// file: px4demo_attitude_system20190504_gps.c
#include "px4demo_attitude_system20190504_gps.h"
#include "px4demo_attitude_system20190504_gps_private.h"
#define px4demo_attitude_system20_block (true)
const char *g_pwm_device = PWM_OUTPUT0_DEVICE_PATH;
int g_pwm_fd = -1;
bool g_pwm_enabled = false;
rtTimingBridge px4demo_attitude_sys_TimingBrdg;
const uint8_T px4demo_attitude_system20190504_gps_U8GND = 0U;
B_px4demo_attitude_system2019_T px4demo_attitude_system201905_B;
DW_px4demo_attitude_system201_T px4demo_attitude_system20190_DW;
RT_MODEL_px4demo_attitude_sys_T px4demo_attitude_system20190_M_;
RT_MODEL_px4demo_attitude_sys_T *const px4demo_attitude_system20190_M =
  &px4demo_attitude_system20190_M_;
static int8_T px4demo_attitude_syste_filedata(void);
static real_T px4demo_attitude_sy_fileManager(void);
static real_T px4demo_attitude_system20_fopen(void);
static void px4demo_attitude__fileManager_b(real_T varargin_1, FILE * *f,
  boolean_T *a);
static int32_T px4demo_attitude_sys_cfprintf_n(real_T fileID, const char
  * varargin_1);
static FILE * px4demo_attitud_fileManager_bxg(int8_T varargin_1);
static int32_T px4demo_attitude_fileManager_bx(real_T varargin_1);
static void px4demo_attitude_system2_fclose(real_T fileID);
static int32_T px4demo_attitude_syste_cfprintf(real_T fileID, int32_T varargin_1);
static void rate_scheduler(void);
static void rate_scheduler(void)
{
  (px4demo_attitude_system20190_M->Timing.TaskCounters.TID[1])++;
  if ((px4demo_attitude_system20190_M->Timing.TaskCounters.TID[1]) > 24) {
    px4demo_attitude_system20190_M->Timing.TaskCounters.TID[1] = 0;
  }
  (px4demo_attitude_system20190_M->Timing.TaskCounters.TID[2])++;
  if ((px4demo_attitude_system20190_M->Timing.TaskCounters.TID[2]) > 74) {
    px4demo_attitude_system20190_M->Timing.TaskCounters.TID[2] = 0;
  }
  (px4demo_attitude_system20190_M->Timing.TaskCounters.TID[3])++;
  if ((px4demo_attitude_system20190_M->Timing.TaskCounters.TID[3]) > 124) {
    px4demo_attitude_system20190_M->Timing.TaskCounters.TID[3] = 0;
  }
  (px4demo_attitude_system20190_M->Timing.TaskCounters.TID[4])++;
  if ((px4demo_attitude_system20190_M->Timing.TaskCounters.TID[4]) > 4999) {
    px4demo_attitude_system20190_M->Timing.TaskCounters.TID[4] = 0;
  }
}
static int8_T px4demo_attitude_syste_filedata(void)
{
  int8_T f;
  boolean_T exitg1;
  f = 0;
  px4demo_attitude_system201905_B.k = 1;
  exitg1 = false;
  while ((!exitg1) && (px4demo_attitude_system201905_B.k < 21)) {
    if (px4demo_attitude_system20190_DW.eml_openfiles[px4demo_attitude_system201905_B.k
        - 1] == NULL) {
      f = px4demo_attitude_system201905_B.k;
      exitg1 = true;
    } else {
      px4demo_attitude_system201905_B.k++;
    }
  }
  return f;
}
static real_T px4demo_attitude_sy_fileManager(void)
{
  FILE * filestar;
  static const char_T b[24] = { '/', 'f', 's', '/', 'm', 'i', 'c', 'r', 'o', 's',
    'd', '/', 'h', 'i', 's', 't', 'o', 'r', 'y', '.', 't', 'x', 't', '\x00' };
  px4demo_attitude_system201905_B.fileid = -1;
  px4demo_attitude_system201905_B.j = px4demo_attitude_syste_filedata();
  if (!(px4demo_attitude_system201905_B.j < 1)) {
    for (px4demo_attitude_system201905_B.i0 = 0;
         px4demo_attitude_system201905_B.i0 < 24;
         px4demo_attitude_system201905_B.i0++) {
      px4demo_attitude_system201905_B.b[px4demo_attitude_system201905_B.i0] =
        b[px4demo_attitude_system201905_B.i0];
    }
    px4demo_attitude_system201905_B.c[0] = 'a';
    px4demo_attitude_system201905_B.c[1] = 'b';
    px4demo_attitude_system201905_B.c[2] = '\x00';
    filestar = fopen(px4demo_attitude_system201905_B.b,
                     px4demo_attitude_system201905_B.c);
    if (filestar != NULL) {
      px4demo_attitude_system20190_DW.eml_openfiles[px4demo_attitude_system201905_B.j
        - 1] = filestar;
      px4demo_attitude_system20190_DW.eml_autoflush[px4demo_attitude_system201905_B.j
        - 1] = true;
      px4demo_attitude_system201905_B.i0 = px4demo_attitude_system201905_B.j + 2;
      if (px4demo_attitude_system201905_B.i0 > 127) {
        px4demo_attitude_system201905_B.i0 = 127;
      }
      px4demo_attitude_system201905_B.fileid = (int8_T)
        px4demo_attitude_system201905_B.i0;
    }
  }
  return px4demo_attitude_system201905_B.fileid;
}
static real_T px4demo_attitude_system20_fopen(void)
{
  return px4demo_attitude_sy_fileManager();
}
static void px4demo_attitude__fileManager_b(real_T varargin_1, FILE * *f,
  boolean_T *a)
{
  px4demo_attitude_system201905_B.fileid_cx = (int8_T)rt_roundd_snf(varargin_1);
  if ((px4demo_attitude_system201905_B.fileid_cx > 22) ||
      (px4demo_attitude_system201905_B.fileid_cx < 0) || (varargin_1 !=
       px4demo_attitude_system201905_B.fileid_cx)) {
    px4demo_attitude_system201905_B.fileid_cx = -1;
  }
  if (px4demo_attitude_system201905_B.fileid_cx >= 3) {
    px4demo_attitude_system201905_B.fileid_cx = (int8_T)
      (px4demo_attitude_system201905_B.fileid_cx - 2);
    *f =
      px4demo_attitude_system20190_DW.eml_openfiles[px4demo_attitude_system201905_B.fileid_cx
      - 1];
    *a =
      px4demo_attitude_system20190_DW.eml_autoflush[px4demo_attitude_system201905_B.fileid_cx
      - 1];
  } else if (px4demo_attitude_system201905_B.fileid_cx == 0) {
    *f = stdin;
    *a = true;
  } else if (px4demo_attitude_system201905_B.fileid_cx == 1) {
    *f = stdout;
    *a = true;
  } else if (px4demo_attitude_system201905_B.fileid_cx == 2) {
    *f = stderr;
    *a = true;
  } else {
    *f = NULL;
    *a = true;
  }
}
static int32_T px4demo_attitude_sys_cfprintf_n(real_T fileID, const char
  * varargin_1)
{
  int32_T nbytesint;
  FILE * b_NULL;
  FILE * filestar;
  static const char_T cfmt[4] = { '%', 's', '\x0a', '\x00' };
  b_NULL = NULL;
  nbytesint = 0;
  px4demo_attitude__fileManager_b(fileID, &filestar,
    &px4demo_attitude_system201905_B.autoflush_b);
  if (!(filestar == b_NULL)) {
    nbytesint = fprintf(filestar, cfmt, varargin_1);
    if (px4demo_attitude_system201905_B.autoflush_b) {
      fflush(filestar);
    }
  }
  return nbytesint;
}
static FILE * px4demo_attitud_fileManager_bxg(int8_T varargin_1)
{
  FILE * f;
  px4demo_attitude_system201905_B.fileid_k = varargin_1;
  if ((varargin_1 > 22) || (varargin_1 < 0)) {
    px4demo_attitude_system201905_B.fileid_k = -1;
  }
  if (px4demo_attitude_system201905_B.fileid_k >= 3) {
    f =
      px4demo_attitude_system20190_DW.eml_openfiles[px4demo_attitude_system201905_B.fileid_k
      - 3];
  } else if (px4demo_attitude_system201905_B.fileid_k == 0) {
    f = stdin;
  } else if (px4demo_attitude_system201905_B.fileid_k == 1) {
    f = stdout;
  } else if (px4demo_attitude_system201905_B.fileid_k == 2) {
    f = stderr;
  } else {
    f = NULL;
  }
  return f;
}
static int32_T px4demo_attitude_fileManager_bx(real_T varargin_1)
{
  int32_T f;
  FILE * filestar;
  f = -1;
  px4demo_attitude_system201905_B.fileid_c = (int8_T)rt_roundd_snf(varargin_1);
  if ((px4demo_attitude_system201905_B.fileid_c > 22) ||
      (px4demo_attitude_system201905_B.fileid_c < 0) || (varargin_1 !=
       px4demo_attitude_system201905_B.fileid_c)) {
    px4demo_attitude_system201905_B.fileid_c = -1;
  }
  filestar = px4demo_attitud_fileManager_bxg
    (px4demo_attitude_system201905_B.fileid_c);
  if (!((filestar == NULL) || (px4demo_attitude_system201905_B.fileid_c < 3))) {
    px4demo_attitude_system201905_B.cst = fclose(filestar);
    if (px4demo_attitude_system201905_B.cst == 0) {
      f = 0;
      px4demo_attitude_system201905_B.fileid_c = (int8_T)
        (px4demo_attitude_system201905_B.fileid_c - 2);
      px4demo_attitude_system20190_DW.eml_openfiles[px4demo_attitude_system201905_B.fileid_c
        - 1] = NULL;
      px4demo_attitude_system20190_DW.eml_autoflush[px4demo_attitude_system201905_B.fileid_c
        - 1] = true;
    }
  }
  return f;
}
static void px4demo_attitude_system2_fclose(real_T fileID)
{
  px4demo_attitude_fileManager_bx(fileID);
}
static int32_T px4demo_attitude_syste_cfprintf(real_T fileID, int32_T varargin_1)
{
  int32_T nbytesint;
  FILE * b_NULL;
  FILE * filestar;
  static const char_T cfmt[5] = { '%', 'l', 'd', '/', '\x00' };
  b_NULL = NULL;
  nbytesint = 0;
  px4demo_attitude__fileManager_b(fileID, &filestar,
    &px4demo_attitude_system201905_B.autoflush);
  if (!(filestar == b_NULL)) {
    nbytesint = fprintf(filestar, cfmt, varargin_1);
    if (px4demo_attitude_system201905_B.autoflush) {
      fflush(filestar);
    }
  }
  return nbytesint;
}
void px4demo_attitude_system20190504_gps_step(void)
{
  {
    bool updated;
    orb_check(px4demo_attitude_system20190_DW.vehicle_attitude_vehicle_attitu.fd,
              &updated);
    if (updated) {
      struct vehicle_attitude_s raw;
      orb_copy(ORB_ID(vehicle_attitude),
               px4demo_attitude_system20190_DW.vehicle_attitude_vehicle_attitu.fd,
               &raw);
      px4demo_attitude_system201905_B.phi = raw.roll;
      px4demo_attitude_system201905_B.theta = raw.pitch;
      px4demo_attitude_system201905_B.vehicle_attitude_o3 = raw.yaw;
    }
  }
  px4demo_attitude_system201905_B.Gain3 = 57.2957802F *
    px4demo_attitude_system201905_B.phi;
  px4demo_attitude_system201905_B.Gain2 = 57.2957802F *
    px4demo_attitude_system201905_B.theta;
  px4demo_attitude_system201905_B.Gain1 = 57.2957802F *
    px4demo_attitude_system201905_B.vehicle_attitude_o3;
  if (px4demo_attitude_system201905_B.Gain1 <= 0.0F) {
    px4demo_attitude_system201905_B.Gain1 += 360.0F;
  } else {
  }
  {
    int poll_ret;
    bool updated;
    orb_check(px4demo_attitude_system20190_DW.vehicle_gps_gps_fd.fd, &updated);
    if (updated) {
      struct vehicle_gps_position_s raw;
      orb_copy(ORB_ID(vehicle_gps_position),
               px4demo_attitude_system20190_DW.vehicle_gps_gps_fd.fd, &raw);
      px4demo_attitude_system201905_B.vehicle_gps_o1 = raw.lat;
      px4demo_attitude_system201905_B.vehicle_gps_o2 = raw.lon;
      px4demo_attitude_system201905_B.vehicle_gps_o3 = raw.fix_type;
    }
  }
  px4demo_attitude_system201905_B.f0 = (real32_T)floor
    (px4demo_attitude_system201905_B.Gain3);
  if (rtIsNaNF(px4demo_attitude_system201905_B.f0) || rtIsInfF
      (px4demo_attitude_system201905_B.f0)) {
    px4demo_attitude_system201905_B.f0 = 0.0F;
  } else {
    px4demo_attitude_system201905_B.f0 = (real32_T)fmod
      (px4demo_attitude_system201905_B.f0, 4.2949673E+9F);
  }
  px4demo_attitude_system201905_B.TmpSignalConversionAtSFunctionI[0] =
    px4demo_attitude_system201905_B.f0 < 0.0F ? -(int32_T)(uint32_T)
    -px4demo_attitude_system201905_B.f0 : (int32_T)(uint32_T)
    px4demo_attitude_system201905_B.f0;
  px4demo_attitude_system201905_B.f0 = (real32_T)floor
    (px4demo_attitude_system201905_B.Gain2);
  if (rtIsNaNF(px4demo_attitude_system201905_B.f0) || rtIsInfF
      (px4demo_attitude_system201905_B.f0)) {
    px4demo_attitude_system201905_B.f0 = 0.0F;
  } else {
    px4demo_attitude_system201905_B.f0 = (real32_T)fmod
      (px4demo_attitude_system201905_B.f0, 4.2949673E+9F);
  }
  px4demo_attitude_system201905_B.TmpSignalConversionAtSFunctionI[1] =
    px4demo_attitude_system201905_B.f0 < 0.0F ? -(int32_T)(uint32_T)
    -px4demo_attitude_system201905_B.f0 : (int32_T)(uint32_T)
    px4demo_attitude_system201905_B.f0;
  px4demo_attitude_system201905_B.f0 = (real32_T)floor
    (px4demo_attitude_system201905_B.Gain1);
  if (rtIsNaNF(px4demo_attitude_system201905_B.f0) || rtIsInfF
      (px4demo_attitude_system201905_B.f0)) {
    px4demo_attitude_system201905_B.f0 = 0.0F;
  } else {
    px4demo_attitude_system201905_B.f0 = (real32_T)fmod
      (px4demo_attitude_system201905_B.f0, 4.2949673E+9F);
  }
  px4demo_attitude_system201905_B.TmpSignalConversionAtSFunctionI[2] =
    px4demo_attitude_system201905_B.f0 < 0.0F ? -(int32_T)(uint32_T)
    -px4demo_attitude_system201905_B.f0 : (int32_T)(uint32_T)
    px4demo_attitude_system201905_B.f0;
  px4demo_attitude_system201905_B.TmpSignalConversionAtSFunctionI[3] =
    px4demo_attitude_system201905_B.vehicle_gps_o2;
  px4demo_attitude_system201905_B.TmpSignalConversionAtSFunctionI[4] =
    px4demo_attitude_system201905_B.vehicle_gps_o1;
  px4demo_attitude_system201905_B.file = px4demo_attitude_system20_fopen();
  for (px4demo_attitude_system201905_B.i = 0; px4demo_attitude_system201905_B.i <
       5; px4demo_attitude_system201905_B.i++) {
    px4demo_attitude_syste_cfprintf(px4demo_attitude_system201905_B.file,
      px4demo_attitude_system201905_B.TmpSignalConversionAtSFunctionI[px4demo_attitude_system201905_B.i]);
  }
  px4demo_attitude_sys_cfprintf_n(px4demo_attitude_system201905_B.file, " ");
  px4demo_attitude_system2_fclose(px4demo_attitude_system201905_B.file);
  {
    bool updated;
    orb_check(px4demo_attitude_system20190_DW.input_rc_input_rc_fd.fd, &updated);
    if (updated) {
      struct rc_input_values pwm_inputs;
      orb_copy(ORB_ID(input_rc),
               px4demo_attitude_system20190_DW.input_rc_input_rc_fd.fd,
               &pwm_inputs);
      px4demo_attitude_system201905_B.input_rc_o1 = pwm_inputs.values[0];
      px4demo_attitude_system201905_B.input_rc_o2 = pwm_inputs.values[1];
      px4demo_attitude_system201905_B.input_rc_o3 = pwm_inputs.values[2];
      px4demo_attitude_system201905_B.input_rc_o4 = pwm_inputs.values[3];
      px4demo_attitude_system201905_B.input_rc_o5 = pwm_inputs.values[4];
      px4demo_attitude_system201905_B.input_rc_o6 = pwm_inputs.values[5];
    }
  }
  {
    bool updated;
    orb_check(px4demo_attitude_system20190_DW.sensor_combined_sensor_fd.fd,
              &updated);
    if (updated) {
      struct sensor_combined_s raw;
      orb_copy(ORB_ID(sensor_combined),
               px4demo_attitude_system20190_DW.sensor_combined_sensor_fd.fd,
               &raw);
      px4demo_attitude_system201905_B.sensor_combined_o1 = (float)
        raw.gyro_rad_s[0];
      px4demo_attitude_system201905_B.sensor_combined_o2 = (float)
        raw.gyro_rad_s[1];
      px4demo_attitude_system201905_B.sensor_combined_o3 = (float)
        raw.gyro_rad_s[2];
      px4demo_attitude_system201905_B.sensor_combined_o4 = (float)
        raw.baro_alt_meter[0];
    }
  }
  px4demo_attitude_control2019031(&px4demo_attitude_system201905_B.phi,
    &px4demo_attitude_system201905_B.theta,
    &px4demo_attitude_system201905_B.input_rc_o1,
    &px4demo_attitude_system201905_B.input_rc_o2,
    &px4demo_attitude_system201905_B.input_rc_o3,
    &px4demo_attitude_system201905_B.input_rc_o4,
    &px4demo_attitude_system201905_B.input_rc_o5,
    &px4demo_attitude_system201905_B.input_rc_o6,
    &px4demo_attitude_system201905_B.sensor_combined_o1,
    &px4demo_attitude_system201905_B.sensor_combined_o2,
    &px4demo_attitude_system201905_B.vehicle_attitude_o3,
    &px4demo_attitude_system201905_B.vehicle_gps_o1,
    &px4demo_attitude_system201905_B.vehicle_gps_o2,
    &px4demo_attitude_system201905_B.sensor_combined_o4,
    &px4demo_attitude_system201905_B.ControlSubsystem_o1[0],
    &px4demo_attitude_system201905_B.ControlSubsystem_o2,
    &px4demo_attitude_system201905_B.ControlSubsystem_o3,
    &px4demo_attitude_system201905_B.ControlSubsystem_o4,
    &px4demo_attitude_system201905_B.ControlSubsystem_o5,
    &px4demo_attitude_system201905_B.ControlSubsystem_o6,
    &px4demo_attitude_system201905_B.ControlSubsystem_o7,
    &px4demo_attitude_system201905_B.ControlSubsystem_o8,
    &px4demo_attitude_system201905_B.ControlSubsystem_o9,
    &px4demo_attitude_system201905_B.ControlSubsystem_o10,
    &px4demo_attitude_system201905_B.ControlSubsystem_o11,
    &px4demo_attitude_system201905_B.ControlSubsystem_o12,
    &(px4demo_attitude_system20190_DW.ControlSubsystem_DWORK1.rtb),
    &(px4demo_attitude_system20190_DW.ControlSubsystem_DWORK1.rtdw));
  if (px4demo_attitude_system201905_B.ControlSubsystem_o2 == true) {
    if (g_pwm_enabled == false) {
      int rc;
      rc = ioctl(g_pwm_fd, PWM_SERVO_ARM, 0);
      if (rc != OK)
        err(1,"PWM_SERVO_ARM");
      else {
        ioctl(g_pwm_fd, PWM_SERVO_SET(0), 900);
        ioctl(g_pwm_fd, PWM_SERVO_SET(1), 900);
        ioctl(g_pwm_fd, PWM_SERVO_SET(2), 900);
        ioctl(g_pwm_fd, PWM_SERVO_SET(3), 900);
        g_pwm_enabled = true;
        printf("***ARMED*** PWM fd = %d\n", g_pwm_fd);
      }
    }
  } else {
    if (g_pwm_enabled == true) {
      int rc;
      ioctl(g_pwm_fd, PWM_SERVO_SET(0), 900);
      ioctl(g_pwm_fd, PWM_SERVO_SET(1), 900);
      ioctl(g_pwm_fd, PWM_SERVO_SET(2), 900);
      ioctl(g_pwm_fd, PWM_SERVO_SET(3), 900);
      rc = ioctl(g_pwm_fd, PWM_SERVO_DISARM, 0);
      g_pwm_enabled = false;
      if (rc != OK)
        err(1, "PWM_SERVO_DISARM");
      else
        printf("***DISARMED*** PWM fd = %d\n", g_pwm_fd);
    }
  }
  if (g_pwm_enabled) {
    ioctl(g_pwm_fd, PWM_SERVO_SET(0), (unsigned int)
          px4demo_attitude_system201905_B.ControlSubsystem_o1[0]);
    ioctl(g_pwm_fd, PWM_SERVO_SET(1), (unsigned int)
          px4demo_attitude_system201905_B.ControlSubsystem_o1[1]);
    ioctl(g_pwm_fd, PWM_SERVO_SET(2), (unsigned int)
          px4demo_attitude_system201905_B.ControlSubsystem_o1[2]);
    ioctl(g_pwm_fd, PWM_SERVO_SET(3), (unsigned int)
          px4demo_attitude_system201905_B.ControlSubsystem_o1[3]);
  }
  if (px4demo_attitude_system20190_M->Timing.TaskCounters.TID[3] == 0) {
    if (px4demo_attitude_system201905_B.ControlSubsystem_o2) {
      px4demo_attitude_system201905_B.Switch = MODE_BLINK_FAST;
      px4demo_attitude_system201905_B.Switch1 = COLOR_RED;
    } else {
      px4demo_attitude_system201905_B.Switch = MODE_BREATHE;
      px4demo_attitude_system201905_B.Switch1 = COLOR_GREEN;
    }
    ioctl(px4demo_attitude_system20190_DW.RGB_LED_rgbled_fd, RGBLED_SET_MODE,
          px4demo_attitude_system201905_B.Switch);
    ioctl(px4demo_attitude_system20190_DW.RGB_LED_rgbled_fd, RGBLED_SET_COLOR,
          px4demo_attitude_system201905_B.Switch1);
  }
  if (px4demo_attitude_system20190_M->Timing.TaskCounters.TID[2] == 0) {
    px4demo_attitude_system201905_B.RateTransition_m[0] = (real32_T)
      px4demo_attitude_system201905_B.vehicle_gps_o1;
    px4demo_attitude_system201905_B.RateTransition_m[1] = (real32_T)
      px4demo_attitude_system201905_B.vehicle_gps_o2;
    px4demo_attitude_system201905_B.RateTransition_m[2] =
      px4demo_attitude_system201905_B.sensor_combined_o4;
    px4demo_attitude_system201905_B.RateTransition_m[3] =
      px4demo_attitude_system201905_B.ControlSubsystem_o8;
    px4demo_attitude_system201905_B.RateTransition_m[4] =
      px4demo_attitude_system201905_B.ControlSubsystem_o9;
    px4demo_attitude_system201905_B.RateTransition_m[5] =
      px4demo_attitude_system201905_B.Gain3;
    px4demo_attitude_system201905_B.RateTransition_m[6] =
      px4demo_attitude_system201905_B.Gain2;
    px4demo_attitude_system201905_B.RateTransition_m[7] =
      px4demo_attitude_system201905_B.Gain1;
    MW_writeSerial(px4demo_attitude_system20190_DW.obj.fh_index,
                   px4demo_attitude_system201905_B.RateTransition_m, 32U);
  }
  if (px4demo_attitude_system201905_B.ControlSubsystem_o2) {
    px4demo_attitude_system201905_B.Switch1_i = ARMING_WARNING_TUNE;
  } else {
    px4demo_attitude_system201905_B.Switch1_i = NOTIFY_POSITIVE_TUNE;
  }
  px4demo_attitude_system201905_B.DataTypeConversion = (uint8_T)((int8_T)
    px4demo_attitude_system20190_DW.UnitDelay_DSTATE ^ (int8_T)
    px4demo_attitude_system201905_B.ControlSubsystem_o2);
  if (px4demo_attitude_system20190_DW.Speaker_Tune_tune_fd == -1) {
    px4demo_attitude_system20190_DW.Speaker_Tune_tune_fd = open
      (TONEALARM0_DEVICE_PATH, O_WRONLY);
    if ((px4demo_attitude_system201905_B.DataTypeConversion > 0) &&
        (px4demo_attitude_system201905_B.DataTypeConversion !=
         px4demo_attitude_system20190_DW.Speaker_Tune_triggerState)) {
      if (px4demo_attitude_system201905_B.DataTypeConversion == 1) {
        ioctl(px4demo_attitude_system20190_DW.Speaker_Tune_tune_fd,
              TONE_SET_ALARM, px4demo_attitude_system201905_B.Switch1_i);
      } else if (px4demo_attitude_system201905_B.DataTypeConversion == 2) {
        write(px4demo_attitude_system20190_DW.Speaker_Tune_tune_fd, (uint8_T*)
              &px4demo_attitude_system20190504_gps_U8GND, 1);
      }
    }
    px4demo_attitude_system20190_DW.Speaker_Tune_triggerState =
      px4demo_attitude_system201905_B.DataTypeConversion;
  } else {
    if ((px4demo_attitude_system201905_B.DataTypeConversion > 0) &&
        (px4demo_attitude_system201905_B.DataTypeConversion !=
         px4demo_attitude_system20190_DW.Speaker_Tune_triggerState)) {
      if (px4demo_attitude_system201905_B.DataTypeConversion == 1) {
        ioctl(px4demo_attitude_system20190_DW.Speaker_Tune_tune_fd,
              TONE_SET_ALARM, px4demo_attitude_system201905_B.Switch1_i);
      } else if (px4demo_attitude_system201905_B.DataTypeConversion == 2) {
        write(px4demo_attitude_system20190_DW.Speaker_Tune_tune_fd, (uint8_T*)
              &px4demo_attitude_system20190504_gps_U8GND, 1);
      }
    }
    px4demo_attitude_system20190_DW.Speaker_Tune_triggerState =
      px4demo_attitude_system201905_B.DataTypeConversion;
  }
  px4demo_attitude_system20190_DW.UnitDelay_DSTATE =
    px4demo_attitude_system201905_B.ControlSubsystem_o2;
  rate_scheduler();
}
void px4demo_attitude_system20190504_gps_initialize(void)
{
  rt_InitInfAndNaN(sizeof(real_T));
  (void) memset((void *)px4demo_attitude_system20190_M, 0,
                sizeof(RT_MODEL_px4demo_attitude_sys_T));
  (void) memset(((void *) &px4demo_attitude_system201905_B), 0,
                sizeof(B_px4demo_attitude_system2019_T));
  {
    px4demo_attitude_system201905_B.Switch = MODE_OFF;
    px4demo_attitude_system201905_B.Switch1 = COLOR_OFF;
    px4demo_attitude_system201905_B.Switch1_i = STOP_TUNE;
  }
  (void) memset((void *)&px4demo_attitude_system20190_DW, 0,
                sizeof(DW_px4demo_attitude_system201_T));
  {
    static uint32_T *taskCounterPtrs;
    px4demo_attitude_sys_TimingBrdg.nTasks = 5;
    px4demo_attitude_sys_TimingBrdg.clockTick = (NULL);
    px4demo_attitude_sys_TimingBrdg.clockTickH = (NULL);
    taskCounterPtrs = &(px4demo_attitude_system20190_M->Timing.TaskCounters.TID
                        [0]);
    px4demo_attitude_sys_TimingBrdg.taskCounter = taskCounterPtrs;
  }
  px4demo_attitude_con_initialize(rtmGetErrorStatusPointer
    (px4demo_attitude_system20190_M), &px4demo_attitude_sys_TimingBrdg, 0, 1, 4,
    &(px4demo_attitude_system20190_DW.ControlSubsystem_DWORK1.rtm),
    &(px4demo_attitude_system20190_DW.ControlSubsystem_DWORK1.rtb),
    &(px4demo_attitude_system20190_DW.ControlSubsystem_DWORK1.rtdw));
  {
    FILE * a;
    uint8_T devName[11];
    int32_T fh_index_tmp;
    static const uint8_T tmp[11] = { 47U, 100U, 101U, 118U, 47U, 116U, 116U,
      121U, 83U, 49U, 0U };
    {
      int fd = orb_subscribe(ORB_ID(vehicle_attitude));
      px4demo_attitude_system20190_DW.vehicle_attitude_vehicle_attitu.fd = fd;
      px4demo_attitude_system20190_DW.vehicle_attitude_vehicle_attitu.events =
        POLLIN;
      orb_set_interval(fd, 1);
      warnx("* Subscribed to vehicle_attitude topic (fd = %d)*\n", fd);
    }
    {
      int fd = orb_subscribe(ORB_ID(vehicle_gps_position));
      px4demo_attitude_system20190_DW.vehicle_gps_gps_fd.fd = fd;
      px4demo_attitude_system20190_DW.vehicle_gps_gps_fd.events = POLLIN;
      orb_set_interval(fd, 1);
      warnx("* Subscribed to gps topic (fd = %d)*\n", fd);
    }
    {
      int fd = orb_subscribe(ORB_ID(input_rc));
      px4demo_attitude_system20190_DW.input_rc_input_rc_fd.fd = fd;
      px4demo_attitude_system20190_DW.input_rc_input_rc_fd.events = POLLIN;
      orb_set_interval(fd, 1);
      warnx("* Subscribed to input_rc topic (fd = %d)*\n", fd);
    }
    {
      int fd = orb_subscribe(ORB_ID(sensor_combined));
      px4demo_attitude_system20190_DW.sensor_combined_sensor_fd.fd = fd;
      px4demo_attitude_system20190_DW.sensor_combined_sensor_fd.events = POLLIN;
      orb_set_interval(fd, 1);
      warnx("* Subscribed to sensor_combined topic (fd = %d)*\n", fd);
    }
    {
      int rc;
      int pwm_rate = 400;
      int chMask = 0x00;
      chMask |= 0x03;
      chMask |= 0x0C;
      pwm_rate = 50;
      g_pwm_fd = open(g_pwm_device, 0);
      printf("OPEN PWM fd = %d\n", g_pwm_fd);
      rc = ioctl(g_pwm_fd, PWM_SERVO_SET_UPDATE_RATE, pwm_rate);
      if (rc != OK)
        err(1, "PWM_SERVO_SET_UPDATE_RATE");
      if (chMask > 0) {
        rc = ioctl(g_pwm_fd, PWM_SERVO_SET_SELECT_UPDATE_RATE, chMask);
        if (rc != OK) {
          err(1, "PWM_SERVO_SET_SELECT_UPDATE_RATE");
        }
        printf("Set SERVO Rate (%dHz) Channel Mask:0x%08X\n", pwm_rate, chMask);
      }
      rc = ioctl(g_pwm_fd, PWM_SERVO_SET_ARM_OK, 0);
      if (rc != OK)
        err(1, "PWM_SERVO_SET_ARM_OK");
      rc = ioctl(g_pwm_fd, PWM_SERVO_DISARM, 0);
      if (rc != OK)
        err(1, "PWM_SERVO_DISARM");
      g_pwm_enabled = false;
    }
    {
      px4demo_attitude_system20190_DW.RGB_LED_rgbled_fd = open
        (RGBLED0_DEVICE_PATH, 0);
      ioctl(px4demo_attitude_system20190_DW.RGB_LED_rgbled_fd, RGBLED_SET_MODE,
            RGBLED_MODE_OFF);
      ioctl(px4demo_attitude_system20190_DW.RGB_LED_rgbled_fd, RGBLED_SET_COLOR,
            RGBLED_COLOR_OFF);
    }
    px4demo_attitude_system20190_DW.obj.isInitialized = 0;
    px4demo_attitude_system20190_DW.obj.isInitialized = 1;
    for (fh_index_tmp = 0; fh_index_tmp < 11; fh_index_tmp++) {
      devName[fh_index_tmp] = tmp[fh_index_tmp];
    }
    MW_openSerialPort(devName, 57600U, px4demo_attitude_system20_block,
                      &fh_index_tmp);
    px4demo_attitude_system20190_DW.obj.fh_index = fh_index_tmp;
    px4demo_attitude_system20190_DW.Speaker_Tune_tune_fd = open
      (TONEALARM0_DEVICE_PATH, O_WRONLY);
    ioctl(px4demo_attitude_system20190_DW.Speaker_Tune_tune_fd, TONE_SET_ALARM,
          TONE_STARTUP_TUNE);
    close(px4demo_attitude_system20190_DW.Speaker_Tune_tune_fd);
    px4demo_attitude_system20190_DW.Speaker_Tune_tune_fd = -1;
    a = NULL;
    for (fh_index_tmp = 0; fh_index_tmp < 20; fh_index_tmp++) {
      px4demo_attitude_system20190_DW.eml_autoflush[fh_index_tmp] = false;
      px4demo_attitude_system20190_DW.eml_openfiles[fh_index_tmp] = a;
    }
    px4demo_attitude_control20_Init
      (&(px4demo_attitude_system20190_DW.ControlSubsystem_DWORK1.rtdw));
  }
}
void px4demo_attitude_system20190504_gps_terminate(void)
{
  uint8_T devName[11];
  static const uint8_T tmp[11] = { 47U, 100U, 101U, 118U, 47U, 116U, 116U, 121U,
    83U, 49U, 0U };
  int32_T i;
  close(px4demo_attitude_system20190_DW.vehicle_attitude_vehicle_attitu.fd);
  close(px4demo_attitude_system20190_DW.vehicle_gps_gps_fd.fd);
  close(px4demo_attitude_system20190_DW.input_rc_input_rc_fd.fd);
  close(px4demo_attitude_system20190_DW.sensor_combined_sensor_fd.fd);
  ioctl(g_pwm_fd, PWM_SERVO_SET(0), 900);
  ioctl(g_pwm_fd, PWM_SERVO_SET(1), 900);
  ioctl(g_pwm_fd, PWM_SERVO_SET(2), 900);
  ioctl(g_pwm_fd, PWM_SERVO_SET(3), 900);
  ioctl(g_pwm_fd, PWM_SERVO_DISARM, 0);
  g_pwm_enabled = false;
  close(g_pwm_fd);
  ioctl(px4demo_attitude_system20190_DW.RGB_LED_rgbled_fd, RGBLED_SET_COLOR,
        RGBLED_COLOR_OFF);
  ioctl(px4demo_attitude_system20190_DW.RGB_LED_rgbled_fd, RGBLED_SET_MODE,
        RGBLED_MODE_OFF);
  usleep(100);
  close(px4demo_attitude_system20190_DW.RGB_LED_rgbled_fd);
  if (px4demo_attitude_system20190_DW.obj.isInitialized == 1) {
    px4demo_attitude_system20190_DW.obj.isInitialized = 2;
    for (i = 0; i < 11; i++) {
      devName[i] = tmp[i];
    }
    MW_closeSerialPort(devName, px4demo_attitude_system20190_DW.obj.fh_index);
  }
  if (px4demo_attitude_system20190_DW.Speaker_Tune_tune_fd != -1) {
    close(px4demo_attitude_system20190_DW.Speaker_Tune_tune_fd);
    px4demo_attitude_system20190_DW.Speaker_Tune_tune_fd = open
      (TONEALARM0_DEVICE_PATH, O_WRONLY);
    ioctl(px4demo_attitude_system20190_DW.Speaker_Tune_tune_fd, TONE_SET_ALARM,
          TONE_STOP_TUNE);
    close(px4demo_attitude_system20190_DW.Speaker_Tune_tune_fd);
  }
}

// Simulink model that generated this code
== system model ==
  MATLABFunction#1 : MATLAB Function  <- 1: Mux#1
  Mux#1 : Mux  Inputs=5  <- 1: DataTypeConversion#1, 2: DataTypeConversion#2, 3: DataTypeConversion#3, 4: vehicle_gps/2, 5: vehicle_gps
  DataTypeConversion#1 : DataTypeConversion  <- 1: Gain3
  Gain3 : Gain  Gain=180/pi  <- 1: DataTypeConversion#4
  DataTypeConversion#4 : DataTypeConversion  <- 1: vehicle_attitude
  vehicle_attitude : pixhawk_slib_sensors_actuators/vehicle_attitude
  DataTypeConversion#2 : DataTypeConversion  <- 1: Gain2
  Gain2 : Gain  Gain=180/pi  <- 1: DataTypeConversion#5
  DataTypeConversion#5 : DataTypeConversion  <- 1: vehicle_attitude/2
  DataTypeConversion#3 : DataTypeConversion  <- 1: MATLABFunction#2
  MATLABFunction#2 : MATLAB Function  <- 1: Gain1
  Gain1 : Gain  Gain=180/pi  <- 1: DataTypeConversion#6
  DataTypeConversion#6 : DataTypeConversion  <- 1: vehicle_attitude/3
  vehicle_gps : pixhawk_slib_sensors_actuators/vehicle_gps
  PWM_output#1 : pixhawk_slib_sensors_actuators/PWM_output  <- 1: ControlSubsystem/2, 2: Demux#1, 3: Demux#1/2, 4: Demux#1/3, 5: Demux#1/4
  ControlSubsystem : ModelReference  <- 1: vehicle_attitude, 2: vehicle_attitude/2, 3: input_rc, 4: input_rc/2, 5: input_rc/3, 6: input_rc/4, 7: input_rc/5, 8: input_rc/6, 9: sensor_combined, 10: sensor_combined/2, 11: vehicle_attitude/3, 12: vehicle_gps, 13: vehicle_gps/2, 14: sensor_combined/4
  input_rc : pixhawk_slib_sensors_actuators/input_rc
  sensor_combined : pixhawk_slib_sensors_actuators/sensor_combined
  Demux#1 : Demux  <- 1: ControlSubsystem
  RGB_LED : pixhawk_slib_sensors_actuators/RGB_LED  <- 1: Switch, 2: Switch1
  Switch : Switch  Criteria=u2 ~= 0  Threshold=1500  <- 1: Constant#1, 2: ControlSubsystem/2, 3: Constant#2
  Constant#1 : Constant  Value=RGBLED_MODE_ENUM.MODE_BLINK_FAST
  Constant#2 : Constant  Value=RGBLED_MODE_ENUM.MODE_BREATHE
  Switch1 : Switch  Criteria=u2 ~= 0  Threshold=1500  <- 1: Constant#3, 2: ControlSubsystem/2, 3: Constant#4
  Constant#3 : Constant  Value=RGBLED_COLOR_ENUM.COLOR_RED
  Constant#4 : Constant  Value=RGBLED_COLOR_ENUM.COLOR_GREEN
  Serial#1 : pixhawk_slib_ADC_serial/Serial  <- 1: RateTransition
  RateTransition : RateTransition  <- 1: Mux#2
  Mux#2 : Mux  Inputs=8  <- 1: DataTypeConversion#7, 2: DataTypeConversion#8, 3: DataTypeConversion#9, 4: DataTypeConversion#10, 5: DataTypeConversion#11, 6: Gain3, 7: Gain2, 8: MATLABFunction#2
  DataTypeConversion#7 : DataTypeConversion  <- 1: vehicle_gps
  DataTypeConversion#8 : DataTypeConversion  <- 1: vehicle_gps/2
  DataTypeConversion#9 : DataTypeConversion  <- 1: sensor_combined/4
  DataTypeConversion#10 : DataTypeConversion  <- 1: ControlSubsystem/8
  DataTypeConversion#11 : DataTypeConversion  <- 1: ControlSubsystem/9
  Speaker_Tune : pixhawk_slib_sensors_actuators/Speaker_Tune  <- 1: Switch#1, 3: DataTypeConversion
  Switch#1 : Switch  Criteria=u2 ~= 0  Threshold=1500  <- 1: Constant#5, 2: ControlSubsystem/2, 3: Constant#6
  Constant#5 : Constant  Value=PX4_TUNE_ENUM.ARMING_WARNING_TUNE
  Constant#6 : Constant  Value=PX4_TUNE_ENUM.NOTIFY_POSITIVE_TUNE
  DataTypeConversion : DataTypeConversion  <- 1: Logic#1
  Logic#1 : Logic  Operator=XOR  <- 1: UnitDelay, 2: ControlSubsystem/2
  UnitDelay : UnitDelay  <- 1: ControlSubsystem/2
== matlab function MATLABFunction#1 ==
function fcn(data)
    file = fopen('/fs/microsd/history.txt','a');
    for i=1:5
        fprintf(file,'%ld/', data(i))
    end
    fprintf(file,'%s\n', ' ')
    fclose(file);
y = data;

== matlab function MATLABFunction#2 ==
function y = fcn(u)
if(u<=0)
    y=360+u;
else
    y=u
end
